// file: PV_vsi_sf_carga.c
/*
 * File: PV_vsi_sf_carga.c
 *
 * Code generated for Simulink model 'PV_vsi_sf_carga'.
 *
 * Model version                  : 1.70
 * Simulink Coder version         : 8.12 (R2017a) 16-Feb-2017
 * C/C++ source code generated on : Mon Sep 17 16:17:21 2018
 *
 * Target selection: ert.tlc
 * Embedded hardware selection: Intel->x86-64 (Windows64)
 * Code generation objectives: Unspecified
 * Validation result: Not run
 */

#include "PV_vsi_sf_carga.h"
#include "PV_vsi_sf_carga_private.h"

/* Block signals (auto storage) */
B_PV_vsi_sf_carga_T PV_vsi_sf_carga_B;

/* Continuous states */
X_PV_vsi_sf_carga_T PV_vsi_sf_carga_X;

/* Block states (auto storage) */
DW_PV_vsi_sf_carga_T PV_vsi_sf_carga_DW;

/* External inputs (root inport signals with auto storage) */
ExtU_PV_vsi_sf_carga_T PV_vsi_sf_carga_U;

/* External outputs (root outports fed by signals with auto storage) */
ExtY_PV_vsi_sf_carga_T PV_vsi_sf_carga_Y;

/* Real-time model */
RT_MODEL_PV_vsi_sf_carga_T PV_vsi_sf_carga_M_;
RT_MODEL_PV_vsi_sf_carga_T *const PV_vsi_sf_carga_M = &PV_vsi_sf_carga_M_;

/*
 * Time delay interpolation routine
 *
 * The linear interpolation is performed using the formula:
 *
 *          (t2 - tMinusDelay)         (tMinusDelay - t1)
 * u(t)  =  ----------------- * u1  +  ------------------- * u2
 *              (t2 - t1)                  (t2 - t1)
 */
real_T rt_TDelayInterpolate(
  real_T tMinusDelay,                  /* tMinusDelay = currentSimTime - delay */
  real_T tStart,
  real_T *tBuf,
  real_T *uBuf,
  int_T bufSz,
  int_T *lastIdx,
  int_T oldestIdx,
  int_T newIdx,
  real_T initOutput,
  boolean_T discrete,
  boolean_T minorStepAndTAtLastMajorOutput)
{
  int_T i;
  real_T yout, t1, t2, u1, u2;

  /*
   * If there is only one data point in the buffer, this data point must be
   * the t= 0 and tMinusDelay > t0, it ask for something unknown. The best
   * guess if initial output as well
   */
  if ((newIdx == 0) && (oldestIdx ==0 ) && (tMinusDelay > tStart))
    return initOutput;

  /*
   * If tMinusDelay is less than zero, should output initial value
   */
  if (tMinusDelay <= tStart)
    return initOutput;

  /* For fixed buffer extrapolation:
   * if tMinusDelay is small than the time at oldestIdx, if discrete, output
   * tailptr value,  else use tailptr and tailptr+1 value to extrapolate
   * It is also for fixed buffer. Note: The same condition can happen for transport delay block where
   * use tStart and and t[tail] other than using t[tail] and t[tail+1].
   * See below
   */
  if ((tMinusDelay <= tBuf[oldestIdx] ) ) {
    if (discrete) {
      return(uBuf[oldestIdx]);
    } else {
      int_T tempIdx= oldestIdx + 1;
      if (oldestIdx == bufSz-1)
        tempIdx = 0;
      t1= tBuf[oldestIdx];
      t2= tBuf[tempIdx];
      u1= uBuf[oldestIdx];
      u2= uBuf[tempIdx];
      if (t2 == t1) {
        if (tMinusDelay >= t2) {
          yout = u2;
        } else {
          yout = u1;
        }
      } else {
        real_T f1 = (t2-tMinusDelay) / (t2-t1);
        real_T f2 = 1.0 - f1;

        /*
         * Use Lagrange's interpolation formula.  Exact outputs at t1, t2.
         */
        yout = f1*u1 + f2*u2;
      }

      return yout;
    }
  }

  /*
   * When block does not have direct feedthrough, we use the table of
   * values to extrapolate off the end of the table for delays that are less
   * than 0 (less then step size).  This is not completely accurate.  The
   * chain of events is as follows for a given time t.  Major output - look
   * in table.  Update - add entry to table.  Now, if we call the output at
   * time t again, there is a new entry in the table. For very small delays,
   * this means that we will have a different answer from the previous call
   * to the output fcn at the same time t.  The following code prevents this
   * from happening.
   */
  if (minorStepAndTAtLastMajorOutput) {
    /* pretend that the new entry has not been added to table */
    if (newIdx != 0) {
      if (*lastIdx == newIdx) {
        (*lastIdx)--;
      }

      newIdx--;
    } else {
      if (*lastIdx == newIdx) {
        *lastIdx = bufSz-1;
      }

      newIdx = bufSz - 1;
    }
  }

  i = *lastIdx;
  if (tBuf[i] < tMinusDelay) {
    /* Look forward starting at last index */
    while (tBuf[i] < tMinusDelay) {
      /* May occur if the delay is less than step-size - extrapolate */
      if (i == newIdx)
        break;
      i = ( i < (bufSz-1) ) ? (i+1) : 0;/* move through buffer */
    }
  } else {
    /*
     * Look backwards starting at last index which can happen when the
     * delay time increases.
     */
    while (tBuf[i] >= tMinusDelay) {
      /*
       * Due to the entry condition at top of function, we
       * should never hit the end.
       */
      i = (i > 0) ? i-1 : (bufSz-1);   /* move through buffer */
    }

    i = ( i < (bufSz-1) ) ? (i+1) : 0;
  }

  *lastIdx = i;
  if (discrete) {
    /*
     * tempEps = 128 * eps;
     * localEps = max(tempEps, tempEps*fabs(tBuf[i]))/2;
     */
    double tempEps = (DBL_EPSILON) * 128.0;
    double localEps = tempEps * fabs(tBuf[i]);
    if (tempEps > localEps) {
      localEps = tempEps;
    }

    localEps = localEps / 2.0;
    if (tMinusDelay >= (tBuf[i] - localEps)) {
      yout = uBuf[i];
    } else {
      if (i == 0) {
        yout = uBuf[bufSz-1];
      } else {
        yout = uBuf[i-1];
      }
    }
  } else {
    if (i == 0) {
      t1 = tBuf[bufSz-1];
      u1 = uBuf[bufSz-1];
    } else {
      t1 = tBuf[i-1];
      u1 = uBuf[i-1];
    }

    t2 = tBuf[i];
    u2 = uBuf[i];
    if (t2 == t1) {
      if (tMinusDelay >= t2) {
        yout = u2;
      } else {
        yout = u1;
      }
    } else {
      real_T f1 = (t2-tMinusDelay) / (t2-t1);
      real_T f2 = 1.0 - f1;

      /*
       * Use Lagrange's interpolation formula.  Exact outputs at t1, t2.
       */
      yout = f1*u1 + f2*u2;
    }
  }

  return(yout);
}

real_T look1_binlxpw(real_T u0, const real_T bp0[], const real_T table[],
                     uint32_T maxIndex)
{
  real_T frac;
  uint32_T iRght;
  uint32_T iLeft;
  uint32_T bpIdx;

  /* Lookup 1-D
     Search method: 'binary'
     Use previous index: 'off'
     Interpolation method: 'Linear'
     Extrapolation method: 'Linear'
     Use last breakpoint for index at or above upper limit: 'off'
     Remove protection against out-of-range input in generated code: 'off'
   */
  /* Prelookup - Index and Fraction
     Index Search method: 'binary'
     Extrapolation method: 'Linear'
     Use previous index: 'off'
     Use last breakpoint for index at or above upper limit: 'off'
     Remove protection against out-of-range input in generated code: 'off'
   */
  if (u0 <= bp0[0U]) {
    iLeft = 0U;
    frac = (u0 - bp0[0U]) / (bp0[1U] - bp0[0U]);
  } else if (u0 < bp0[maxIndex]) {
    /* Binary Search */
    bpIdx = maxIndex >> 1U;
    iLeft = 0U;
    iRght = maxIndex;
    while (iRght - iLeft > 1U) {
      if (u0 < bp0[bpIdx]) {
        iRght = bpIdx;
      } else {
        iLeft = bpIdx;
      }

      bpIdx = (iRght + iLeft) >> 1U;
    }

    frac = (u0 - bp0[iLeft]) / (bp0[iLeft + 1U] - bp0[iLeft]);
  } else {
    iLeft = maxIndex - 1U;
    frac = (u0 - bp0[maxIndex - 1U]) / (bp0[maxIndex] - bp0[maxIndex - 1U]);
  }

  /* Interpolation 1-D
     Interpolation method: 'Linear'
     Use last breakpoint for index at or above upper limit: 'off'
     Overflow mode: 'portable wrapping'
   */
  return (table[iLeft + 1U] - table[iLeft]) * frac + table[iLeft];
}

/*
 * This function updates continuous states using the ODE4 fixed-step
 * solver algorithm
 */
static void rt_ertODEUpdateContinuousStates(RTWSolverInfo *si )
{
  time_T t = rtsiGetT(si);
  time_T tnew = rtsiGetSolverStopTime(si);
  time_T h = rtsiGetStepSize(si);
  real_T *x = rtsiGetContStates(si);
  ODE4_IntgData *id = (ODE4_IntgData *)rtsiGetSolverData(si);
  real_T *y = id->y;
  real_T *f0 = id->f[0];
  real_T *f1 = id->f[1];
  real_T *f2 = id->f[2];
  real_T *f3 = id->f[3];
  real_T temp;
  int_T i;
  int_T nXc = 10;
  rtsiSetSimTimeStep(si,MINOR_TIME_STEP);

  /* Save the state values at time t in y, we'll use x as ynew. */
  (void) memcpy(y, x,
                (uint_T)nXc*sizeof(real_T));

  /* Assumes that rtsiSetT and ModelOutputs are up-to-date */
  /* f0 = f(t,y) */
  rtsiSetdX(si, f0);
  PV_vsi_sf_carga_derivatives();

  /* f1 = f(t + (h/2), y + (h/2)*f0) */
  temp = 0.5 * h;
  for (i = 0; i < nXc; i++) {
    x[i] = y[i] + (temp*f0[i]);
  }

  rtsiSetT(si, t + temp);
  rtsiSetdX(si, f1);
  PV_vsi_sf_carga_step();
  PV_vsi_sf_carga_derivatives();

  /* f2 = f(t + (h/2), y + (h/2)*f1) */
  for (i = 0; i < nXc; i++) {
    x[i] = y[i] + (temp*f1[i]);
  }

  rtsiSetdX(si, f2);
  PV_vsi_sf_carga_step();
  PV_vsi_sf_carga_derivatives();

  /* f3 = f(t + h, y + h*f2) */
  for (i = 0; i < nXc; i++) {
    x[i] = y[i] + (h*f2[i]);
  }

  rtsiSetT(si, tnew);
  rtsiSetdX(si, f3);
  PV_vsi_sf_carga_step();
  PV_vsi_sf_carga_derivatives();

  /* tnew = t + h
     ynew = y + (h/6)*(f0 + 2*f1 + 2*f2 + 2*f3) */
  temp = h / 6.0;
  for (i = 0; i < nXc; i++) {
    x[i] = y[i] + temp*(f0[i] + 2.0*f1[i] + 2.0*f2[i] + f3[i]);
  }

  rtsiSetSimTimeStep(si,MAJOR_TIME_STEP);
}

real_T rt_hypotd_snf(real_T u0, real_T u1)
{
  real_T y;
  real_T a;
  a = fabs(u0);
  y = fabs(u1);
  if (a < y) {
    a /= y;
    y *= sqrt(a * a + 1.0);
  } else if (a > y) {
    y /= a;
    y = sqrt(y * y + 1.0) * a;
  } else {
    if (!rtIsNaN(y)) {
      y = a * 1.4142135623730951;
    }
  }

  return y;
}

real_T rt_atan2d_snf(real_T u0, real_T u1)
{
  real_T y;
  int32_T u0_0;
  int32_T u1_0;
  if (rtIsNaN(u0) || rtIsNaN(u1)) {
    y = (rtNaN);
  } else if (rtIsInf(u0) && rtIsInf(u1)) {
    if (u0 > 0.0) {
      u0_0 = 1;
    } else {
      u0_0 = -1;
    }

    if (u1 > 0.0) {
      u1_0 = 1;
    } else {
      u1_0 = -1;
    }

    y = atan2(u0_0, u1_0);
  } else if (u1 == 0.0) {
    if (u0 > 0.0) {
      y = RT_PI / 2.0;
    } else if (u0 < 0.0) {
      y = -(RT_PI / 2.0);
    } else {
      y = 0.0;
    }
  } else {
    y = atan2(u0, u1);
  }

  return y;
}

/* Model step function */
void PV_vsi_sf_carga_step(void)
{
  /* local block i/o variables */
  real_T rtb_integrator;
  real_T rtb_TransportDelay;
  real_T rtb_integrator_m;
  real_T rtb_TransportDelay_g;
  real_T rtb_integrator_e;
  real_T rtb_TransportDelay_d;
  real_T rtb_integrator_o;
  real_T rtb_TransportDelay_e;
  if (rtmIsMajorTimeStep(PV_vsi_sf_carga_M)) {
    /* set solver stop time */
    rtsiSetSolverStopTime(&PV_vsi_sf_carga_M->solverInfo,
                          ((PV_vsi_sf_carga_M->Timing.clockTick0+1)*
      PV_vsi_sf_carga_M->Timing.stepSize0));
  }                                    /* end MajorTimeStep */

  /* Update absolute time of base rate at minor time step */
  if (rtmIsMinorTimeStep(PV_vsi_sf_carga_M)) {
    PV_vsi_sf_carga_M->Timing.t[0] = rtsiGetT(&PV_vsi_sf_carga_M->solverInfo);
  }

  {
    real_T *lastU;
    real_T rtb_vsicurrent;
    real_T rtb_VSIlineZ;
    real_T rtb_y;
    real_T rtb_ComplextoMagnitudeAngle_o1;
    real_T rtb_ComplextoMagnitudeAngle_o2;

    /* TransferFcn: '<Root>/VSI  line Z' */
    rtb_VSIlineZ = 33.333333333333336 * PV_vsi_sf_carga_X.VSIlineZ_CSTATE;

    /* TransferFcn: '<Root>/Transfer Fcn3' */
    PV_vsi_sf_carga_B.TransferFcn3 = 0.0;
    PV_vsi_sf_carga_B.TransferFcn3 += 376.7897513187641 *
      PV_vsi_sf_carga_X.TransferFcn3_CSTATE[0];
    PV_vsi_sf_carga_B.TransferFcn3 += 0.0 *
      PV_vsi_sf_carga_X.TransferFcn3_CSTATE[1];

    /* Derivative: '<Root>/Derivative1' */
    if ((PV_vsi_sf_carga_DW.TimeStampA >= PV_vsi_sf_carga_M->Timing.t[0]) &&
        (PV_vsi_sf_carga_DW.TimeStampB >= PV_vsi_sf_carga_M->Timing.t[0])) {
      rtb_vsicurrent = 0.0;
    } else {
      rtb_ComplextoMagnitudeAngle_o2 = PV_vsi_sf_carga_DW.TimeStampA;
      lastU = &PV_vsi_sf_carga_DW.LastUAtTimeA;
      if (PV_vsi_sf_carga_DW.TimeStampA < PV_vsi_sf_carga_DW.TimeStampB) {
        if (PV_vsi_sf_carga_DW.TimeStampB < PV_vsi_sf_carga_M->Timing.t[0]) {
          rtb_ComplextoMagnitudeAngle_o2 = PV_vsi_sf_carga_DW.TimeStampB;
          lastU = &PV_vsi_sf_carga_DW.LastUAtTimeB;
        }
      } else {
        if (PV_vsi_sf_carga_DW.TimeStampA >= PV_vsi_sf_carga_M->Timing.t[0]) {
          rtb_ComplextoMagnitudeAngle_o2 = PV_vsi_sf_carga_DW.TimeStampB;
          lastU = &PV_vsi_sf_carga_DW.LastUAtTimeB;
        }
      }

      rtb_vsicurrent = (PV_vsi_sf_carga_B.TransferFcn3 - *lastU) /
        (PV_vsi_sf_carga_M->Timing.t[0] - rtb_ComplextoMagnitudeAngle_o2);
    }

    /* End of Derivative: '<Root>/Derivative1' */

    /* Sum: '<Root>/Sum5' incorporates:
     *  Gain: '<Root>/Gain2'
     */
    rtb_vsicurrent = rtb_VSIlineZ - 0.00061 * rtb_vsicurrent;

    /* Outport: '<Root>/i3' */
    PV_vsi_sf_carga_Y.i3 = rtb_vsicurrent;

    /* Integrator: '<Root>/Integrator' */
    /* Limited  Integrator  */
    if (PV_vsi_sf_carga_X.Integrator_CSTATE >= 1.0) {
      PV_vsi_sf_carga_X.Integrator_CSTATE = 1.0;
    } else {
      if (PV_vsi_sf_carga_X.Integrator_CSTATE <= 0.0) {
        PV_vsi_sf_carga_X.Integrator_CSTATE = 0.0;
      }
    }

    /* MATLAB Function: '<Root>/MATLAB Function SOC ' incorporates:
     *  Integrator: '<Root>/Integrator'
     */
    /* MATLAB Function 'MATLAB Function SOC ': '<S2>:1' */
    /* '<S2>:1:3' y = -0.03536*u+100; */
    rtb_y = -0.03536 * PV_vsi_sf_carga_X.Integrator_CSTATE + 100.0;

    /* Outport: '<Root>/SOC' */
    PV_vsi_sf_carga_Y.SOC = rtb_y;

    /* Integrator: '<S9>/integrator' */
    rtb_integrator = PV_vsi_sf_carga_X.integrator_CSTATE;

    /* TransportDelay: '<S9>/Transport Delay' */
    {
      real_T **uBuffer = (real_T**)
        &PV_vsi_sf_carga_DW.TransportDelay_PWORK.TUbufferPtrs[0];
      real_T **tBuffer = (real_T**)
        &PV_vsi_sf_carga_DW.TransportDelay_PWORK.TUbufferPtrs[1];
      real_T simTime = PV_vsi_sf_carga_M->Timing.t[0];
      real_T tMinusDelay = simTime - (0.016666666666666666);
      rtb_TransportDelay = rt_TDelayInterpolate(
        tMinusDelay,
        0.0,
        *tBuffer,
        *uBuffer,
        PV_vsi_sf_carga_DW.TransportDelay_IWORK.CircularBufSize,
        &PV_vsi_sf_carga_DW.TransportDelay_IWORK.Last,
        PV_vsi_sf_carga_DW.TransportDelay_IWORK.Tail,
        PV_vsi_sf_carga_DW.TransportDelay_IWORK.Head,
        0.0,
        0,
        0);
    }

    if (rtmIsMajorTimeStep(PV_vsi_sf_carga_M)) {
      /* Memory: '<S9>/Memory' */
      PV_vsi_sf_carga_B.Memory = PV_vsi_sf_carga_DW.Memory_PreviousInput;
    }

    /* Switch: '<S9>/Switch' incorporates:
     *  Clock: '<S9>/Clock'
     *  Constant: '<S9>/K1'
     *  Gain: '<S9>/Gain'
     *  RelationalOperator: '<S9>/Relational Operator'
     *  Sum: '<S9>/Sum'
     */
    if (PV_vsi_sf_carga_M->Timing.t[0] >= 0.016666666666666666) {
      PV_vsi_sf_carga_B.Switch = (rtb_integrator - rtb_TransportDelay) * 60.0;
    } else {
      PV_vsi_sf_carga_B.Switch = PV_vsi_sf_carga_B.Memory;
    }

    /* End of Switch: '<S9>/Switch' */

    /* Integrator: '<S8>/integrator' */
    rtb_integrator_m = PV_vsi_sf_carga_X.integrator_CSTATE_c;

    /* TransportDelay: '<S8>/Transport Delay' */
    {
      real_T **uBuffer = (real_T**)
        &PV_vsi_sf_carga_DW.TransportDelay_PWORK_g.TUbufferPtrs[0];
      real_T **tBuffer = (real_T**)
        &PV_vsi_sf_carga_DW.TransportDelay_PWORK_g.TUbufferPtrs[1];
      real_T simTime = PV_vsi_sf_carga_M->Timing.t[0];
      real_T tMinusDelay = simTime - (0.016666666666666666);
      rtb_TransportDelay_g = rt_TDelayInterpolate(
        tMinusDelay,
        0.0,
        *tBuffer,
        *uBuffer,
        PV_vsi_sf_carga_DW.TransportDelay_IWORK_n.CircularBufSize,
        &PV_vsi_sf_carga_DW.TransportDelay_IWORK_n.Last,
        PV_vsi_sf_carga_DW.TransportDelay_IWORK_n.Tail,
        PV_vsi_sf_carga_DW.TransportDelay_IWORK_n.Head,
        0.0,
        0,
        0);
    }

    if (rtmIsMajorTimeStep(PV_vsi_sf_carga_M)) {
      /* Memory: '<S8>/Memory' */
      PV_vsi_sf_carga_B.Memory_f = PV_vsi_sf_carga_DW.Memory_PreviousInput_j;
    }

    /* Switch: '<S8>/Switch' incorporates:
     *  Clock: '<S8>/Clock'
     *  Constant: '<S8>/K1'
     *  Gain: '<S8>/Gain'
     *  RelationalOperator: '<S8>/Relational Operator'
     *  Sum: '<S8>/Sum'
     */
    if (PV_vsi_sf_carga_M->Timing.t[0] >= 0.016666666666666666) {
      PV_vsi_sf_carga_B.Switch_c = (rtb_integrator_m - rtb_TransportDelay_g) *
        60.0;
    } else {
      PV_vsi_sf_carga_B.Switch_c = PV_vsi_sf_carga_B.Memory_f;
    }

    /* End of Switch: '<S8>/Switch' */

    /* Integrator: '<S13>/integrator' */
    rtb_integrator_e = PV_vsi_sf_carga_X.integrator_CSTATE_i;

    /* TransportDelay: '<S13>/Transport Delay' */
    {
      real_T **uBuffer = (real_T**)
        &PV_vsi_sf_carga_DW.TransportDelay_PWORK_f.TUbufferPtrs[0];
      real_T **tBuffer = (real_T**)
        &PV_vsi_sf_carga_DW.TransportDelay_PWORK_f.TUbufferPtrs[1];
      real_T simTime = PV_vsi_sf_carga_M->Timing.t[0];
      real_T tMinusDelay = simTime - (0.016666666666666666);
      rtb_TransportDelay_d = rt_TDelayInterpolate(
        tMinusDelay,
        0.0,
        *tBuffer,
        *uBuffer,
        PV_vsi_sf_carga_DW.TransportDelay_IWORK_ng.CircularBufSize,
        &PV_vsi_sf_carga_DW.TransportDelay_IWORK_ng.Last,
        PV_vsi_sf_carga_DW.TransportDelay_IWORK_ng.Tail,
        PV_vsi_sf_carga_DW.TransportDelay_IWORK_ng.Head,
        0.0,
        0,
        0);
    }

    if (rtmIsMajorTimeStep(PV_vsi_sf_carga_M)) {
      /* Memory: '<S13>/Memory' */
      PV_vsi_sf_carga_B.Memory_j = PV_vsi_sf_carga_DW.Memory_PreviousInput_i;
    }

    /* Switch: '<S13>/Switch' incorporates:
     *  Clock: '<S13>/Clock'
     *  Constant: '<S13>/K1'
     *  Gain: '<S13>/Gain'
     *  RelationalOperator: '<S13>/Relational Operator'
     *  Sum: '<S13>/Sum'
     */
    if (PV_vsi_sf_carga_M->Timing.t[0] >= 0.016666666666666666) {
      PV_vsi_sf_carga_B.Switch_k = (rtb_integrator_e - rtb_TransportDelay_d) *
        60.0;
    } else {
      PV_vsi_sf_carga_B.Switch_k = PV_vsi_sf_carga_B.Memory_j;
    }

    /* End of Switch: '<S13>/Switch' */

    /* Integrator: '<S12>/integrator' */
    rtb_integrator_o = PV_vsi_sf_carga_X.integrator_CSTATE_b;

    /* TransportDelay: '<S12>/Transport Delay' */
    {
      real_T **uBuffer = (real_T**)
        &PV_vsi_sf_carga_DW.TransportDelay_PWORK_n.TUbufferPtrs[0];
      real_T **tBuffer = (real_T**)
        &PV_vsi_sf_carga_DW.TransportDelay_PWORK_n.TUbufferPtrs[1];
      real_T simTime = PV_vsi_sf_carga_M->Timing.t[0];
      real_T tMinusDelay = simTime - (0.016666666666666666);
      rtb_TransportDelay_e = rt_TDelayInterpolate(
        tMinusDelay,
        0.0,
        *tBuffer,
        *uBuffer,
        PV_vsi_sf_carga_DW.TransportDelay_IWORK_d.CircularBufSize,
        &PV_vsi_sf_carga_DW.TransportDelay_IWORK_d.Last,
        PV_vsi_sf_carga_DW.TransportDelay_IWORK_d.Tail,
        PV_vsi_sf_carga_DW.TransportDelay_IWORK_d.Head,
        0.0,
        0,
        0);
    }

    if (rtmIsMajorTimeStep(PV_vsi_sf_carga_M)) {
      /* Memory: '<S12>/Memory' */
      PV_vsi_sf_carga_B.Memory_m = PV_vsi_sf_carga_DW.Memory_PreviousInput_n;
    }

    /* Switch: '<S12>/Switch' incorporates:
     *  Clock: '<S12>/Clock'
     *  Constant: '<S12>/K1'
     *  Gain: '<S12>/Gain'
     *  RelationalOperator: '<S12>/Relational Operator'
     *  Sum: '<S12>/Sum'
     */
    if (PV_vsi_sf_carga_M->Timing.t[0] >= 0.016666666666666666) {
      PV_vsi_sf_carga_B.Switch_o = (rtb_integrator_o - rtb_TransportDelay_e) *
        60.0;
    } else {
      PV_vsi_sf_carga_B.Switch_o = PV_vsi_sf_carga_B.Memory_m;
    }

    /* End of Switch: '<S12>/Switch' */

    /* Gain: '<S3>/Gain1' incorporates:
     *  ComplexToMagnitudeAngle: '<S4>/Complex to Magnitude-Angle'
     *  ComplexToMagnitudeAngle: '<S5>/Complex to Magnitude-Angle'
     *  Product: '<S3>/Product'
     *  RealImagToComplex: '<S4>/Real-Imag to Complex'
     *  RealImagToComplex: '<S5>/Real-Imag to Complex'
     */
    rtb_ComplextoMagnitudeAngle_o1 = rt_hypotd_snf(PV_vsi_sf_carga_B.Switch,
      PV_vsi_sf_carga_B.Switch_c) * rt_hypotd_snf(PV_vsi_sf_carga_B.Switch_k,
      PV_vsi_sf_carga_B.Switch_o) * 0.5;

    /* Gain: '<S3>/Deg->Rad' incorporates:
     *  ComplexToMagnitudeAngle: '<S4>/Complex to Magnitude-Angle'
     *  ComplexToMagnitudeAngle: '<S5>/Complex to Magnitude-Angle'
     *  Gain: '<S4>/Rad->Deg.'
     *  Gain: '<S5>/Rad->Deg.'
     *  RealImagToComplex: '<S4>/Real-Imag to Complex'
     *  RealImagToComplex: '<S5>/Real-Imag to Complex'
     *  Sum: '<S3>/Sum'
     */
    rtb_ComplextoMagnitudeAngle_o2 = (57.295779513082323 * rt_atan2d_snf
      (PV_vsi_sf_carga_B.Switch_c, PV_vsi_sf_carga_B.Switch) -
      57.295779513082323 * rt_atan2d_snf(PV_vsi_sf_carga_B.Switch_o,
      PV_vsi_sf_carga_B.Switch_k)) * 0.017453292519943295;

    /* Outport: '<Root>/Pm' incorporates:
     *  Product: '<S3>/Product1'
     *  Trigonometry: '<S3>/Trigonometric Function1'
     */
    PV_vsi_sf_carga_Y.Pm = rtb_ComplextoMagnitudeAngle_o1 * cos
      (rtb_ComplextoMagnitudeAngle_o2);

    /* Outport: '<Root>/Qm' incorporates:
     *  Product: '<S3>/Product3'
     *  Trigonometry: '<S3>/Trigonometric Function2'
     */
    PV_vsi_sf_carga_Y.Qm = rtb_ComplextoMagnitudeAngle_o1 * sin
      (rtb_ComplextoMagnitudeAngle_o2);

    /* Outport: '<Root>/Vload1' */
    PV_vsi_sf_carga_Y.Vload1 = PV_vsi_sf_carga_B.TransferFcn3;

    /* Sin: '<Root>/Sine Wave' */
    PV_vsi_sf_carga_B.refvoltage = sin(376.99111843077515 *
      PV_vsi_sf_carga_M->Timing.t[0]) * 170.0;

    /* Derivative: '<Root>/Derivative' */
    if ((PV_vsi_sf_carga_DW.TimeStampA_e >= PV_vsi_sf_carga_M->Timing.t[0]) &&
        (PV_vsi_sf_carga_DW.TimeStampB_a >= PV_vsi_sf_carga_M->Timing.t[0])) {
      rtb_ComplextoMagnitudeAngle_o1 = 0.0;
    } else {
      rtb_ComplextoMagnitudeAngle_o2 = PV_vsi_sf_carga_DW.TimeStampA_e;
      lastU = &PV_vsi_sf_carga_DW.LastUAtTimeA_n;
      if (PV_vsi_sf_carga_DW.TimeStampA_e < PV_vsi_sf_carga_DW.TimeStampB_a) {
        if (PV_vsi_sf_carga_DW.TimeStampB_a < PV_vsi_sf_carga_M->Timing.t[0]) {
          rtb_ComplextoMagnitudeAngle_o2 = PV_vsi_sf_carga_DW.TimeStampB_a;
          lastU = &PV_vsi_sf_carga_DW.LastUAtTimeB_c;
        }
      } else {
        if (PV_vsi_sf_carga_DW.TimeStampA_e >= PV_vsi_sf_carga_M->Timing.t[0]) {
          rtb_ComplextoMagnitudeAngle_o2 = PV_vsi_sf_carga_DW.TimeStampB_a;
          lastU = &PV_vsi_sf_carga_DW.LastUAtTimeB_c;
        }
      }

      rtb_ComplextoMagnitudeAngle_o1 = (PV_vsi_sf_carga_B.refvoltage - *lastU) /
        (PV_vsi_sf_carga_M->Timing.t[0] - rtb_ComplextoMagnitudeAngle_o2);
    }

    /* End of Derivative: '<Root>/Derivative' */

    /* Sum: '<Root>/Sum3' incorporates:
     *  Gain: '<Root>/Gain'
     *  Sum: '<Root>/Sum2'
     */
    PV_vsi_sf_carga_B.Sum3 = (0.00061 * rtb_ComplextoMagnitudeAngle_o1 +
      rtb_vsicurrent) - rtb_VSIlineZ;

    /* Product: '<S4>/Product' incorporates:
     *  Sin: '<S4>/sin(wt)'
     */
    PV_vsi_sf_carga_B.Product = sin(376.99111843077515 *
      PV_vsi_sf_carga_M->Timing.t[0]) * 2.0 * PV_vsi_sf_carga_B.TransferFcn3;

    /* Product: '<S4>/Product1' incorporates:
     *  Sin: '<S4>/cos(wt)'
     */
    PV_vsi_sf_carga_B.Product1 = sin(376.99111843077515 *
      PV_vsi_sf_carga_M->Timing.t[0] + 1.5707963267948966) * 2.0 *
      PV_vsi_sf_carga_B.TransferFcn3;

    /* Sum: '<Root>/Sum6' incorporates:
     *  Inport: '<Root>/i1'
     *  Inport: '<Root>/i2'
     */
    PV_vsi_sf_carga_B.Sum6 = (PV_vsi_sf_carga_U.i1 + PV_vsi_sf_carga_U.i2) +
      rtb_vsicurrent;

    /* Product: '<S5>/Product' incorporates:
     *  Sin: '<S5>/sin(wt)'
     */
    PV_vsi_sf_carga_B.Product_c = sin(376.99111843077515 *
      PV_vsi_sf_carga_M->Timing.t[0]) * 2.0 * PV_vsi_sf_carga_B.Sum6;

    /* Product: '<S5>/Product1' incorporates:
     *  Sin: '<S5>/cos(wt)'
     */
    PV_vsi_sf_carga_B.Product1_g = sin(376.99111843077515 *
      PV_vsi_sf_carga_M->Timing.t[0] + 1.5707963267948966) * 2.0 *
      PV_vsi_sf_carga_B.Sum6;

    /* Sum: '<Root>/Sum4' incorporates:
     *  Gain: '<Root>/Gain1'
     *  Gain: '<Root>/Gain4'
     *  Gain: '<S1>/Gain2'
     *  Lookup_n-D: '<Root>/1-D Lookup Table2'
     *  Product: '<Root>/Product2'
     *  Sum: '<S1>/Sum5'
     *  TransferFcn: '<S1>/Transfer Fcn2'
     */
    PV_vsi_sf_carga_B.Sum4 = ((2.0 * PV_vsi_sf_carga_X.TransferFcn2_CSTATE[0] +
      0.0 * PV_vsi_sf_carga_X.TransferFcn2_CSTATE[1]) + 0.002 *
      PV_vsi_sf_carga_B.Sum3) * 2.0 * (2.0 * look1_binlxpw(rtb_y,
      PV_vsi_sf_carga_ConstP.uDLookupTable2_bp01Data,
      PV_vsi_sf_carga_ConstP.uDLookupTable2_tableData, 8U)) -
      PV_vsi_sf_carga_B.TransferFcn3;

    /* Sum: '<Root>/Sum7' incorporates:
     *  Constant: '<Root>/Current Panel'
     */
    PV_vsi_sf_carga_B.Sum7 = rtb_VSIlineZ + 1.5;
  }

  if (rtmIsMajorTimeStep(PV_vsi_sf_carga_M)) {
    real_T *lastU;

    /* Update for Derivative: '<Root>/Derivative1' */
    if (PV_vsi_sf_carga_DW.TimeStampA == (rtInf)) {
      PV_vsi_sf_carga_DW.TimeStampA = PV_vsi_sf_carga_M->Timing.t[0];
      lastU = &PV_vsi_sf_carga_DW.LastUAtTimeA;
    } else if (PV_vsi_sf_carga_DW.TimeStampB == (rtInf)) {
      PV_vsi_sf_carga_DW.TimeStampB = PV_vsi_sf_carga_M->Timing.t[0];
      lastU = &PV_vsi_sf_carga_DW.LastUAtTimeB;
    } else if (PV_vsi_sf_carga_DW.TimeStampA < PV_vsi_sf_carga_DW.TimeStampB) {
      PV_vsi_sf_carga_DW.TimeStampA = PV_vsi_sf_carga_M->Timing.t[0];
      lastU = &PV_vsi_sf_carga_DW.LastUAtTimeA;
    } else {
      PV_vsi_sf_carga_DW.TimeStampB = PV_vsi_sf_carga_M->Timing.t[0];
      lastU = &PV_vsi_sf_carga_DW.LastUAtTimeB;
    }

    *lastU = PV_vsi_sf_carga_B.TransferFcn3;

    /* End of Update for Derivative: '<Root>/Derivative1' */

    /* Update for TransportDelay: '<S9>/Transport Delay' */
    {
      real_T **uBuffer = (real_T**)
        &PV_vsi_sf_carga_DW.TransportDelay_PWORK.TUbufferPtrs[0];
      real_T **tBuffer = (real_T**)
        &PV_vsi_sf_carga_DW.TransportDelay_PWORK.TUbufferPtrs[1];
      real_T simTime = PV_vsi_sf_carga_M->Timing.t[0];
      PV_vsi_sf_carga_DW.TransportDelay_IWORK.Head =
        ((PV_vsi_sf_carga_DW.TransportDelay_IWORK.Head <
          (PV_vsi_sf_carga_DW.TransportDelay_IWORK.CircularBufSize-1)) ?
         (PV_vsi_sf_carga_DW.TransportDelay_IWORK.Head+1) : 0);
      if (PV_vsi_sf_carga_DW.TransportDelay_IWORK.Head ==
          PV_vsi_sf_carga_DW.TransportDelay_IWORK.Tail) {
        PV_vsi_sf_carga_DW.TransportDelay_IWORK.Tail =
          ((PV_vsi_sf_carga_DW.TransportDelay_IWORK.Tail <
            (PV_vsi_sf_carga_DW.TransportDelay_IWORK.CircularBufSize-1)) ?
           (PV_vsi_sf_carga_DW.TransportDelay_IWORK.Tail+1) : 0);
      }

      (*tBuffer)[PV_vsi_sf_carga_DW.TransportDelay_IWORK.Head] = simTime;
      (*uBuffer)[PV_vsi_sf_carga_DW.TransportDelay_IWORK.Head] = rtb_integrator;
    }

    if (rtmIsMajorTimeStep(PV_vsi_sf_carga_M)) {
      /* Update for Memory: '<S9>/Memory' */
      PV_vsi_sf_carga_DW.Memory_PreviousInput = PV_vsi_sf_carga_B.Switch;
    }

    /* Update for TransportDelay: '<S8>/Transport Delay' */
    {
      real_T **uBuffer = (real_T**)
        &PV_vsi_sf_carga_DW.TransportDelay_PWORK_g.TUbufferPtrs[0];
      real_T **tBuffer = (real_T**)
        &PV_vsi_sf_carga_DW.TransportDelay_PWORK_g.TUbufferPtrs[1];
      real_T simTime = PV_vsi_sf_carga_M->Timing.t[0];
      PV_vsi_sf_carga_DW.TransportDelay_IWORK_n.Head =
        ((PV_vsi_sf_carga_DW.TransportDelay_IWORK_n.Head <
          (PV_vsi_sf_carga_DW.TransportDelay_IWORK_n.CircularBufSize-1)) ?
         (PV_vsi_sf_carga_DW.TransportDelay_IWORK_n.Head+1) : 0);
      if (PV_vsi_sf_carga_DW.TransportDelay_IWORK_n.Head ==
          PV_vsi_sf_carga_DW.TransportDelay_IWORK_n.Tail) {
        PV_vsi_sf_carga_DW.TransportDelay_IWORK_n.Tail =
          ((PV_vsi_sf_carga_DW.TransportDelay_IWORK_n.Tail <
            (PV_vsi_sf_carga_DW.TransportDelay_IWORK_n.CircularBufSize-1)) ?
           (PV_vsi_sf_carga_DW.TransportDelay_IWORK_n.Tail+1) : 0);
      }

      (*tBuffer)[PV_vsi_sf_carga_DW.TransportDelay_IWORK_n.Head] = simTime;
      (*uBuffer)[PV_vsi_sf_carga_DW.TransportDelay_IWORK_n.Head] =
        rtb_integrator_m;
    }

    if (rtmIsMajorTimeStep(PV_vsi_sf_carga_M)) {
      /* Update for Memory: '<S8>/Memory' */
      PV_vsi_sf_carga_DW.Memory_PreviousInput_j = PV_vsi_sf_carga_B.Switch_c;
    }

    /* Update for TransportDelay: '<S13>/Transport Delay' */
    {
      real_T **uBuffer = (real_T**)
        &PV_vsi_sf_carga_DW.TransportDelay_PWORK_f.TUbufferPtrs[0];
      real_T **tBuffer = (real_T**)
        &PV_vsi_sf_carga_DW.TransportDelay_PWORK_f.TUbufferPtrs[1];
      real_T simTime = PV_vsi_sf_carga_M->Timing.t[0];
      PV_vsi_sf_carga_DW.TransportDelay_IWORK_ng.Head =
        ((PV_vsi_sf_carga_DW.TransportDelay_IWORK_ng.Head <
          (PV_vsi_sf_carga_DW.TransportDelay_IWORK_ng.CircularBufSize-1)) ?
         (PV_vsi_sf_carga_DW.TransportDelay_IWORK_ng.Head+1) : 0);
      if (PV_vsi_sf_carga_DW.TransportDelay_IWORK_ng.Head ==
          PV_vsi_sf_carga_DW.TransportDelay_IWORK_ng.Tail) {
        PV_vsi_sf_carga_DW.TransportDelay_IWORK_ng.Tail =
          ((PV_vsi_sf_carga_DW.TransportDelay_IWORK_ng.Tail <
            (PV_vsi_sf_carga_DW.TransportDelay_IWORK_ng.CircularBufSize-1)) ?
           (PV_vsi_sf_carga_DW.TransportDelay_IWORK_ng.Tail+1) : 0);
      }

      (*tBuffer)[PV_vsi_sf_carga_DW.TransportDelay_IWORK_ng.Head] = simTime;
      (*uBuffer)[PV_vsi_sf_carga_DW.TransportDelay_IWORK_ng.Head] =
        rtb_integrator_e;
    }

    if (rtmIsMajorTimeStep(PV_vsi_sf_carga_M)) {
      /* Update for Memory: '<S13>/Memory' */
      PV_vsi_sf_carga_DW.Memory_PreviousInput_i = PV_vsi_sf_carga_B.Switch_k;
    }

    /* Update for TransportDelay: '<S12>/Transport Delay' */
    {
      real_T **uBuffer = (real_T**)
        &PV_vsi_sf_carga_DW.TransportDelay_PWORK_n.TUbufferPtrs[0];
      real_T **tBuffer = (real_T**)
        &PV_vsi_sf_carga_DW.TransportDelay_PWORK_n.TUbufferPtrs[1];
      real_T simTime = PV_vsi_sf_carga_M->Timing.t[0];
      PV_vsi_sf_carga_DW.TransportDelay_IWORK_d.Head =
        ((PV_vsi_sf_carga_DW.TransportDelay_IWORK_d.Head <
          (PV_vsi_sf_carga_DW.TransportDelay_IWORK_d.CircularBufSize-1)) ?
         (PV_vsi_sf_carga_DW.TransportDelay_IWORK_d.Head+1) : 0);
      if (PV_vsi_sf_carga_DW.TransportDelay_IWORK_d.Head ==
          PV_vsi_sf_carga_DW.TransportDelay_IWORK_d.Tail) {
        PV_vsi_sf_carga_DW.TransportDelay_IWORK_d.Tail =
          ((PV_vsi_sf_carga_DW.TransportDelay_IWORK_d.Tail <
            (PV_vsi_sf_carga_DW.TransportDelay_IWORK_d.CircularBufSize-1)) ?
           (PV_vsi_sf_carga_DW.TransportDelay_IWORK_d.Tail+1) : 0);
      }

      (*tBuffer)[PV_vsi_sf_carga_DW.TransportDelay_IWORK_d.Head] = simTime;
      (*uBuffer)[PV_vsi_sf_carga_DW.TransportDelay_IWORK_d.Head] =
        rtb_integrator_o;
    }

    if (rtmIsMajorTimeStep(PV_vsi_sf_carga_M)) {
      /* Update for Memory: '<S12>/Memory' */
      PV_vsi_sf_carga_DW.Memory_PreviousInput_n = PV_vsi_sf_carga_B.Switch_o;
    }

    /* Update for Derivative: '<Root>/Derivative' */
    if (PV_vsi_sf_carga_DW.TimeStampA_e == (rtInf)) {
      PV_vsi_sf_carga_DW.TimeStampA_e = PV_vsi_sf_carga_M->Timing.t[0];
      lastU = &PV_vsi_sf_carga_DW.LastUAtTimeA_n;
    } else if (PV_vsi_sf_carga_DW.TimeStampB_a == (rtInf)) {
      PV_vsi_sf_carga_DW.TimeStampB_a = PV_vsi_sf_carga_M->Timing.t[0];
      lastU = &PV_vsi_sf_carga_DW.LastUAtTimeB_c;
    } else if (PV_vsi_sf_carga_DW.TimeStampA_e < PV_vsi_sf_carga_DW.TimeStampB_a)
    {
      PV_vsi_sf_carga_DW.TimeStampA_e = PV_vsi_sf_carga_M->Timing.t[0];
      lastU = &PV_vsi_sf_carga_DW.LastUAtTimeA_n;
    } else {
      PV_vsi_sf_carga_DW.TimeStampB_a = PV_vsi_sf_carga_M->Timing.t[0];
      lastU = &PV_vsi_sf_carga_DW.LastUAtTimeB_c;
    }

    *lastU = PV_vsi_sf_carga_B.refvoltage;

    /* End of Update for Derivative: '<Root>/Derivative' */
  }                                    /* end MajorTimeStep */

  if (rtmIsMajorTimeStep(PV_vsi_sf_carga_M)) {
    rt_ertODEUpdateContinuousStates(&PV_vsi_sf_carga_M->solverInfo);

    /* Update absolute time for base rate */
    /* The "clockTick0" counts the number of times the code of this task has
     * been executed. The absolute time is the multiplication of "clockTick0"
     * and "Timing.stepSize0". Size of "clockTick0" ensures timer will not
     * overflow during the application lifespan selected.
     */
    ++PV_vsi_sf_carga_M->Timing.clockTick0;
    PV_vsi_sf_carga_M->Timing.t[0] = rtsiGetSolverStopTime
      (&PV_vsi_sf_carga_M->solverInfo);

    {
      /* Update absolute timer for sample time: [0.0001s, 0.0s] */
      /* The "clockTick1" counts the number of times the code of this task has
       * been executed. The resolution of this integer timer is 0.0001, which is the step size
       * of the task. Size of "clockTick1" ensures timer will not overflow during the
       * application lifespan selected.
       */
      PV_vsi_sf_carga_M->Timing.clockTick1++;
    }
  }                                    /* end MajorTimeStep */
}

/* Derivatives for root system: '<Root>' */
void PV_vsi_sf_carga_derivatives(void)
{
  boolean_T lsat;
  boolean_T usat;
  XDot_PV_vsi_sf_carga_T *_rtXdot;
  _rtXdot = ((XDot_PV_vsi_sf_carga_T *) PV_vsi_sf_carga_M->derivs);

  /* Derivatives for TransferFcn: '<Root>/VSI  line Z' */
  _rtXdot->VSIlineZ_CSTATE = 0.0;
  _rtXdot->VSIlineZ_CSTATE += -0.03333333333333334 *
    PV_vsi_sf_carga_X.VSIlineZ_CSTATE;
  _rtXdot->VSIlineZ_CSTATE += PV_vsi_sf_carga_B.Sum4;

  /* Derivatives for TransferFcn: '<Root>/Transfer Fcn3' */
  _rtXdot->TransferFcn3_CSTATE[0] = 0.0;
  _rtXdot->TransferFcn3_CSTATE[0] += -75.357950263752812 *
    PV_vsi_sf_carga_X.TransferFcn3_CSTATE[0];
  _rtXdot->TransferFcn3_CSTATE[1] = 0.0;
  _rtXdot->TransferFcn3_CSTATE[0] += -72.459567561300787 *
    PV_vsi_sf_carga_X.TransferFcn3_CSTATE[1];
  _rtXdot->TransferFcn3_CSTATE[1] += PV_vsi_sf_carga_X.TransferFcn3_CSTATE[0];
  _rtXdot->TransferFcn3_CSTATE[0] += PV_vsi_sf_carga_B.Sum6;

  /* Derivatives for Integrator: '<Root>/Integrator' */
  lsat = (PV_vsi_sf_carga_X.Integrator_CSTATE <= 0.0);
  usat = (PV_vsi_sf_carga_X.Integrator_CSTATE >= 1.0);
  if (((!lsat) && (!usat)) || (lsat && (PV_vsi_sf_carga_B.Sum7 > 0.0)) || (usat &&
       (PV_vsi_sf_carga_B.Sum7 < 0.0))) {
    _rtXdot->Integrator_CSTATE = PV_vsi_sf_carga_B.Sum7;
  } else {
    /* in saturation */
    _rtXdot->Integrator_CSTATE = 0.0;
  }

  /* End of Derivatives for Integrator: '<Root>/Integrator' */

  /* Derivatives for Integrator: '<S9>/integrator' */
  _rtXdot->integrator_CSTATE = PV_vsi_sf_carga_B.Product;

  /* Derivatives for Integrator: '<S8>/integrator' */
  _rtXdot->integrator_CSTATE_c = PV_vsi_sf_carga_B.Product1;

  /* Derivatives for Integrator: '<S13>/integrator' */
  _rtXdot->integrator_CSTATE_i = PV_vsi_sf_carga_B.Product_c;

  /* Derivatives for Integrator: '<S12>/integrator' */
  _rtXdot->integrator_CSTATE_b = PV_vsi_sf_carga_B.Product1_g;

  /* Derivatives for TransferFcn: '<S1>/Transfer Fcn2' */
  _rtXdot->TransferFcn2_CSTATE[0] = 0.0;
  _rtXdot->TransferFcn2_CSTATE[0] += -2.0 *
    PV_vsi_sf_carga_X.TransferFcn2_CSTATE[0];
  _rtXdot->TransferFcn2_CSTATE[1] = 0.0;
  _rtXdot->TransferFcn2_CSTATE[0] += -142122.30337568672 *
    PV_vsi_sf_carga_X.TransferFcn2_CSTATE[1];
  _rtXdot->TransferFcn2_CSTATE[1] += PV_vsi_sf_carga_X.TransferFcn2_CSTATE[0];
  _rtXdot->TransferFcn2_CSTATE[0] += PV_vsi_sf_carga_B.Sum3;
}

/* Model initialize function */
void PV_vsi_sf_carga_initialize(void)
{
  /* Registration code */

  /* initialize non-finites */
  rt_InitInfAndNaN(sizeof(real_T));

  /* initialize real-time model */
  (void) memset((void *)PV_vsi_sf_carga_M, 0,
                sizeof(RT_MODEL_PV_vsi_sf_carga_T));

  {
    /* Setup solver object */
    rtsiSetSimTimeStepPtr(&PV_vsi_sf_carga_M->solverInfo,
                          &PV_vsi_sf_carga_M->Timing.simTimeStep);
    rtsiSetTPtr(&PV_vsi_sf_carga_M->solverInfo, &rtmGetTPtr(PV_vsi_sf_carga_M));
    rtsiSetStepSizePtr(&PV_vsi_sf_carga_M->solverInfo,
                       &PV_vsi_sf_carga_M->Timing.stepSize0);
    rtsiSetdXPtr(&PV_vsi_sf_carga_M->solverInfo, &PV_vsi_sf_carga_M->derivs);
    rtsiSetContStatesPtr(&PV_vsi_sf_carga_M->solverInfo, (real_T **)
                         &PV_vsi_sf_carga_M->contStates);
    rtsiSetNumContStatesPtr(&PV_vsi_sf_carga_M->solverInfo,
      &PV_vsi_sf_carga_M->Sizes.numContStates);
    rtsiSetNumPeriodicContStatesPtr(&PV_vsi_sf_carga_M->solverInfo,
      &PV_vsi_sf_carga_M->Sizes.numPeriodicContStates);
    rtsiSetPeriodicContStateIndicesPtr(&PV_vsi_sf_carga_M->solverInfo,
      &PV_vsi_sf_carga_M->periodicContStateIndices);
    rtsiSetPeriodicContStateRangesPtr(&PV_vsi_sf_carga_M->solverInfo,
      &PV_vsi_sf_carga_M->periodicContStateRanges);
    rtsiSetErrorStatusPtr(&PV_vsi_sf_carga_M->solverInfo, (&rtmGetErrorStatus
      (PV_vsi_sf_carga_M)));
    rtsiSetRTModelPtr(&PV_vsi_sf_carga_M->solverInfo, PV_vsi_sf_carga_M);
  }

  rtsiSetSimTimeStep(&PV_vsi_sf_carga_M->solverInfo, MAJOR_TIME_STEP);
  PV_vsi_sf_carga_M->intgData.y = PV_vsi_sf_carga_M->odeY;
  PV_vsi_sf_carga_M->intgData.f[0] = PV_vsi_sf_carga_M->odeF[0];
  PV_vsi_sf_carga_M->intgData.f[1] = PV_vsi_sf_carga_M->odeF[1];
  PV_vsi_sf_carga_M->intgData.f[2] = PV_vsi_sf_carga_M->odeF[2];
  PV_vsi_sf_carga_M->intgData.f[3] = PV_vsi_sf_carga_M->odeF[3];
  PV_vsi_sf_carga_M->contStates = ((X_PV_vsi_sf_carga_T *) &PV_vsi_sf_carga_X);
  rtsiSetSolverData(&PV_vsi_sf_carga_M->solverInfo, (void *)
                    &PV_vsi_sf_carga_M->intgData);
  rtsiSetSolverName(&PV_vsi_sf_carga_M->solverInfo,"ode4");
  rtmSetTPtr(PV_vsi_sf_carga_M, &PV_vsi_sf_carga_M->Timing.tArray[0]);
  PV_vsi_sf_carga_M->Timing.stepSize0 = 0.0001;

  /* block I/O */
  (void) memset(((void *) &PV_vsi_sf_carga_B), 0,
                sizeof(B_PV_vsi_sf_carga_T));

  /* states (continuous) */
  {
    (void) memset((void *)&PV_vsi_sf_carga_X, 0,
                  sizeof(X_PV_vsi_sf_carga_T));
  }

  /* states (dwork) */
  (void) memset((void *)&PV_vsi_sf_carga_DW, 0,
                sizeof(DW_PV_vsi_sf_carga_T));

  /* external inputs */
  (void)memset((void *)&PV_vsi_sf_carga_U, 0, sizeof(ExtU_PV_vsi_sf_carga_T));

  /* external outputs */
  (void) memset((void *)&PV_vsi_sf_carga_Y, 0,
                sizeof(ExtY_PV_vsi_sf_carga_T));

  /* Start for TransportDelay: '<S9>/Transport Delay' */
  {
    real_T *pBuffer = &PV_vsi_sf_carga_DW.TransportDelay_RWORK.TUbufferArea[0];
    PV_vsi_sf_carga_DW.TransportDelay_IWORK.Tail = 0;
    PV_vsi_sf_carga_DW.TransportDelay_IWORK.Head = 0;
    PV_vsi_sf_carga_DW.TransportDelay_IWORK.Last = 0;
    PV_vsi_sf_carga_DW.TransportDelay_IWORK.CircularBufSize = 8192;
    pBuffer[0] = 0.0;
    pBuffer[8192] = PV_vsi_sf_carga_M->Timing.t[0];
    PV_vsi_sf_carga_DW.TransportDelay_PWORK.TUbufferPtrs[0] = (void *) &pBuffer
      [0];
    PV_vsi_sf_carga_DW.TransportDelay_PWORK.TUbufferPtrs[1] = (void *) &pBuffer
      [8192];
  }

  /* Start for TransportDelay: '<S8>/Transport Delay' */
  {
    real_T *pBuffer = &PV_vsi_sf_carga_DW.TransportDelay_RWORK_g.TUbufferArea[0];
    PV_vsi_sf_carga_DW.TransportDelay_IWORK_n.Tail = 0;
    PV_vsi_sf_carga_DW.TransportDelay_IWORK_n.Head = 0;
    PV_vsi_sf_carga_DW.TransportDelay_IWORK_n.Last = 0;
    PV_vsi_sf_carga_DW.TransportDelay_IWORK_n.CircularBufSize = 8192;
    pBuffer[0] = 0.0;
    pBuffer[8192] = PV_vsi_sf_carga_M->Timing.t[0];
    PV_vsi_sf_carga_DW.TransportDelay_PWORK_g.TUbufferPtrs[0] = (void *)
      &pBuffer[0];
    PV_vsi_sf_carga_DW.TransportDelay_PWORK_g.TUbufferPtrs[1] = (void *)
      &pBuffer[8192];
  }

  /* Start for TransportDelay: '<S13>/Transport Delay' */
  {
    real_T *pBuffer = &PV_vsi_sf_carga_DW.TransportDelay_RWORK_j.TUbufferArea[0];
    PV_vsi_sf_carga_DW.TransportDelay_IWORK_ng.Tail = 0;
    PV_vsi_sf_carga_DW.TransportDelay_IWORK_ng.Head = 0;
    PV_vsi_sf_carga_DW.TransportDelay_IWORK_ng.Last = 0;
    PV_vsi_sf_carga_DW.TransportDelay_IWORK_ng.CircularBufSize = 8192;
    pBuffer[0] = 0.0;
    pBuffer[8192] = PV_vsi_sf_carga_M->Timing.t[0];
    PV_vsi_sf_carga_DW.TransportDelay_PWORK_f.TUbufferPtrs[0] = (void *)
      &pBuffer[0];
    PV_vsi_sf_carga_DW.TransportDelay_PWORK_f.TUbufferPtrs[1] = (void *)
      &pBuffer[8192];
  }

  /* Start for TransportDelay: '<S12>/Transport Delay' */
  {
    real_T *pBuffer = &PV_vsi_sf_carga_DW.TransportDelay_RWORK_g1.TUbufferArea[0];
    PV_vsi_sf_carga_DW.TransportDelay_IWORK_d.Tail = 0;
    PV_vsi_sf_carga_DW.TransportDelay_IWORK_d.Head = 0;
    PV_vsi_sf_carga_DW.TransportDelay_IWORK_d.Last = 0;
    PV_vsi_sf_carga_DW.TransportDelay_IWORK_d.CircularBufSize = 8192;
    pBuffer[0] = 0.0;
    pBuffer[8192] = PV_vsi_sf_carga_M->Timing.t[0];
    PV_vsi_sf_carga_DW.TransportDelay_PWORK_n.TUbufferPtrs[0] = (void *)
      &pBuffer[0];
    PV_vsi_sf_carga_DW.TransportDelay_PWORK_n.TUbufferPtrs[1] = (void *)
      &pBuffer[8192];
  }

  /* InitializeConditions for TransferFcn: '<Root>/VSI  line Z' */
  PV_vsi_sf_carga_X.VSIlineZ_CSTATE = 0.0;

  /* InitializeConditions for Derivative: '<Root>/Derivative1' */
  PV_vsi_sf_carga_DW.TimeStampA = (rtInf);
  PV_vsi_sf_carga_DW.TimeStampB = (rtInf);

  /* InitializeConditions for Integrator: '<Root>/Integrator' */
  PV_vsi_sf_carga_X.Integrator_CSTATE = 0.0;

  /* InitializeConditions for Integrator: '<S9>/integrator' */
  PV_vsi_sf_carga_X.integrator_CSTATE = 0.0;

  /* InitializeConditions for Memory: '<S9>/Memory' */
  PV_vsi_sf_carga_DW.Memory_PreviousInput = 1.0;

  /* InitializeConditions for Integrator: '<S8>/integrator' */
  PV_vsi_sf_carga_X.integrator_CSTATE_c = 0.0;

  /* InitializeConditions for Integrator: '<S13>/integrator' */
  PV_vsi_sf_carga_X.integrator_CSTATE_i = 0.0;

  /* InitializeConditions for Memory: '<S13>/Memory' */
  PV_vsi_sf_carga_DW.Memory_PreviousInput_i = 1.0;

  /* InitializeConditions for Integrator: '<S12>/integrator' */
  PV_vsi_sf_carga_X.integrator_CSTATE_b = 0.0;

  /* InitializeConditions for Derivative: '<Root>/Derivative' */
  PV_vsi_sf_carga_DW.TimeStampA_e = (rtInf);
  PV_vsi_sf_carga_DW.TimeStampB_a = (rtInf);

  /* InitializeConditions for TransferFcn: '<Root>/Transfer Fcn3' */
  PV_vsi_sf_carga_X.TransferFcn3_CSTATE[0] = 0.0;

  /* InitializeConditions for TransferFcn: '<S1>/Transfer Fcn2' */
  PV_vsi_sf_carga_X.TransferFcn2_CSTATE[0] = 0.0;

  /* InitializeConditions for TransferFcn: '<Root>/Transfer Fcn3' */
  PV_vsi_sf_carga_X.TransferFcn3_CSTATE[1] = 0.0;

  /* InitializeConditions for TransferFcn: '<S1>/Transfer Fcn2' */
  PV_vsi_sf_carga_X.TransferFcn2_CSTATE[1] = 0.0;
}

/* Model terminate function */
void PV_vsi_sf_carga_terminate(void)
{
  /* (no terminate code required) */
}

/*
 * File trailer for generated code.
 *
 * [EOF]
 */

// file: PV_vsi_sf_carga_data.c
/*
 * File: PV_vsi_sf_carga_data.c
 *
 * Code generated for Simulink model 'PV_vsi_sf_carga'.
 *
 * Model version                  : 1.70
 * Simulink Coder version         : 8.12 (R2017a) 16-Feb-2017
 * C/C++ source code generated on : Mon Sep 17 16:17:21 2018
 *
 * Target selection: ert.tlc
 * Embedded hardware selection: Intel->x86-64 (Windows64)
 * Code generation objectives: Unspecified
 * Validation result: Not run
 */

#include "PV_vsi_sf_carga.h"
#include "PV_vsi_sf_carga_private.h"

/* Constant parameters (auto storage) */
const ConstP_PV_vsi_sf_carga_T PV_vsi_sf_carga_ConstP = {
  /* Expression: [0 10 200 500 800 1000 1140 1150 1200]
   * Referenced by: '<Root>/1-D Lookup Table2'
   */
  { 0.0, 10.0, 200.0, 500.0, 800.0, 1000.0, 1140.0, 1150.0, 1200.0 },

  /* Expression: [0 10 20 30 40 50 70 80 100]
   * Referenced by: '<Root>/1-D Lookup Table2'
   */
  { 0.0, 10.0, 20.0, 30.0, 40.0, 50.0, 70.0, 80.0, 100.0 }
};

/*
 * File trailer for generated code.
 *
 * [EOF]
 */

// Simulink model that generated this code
simulink model "PV_vsi_sf_carga"  (R2017a)
settings: Solver=ode4  StartTime=0.0  StopTime=6  FixedStep=1e-4  RelTol=1e-3
InitFcn:
  | SimulinkInit
values from neighbouring files (symbols this model uses):
  C = [C11; C22; C33;C44]    [Parametros_Sistema.m]    (also in SimulinkInit.m = 0.002654; SimulinkInit_linea_transmision.m = 1)
  C3 = 610e-6    (= 0.00061)    [Parametros_Sistema.m]    (also in SimulinkInit.m; SimulinkInit_linea_transmision.m; sistema.m)
  L3 = 5e-3    (= 0.005)    [Parametros_Sistema.m]    (also in SimulinkInit.m = 0.03; SimulinkInit_linea_transmision.m; sistema.m)
  L4 = 1e-3    (= 0.001)    [Parametros_Sistema.m]    (also in SimulinkInit.m = 5.2; SimulinkInit_linea_transmision.m = 3.5e-05; sistema.m)
  R3 = 1e-3    (= 0.001)    [Parametros_Sistema.m]    (also in SimulinkInit.m; SimulinkInit_linea_transmision.m; sistema.m)
  R4 = 10    [Parametros_Sistema.m]    (also in SimulinkInit.m; SimulinkInit_linea_transmision.m = 0.005; sistema.m)
  R5 = 4    [Parametros_Sistema.m]    (also in SimulinkInit.m = 10; SimulinkInit_linea_transmision.m = 0.0012; sistema.m)
libraries: powerlib_meascontrol x1

== system PV_vsi_sf_carga ==
  note: VSI
  note: Carga RLC
  Vload : Inport
  Ipv : Inport  Port=2
  i1 : Inport  Port=3
  i2 : Inport  Port=4
  1-D Lookup Table2 : Lookup_n-D  NumberOfTableDimensions=1  BreakpointsForDimension1=[0 10 20 30 40 50 70 80 100]  Table=[0 10 200 500 800 1000 1140 1150 1200]  InternalRulePriority=Speed  RndMeth=Simplest  InputSameDT=on
  Control PR VSI : Subsystem
  Current Panel : Constant  Value=1.5
  Derivative : Derivative
  Derivative1 : Derivative
  Gain : Gain  Gain=C3
  Gain1 : Gain  Gain=2
  Gain2 : Gain  Gain=C3
  Gain4 : Gain  Gain=2
  Integrator : Integrator  LimitOutput=on  UpperSaturationLimit=1  LowerSaturationLimit=0
  "MATLAB Function SOC " : MATLAB Function  TreatAsAtomicUnit=on
  Power : powerlib_meascontrol/Measurements/Power  Freq=60  Vinit=[1, 0]  Iinit=[1, 0]  Ts=0
  Product2 : Product
  Sine Wave : Sin  Amplitude=170  Frequency=2*pi*60  SampleTime=0
  Sum2 : Sum  Inputs=|++
  Sum3 : Sum  Inputs=|+-
  Sum4 : Sum  Inputs=|+-
  Sum5 : Sum  Inputs=|+-
  Sum6 : Sum  Inputs=3
  Sum7 : Sum  Inputs=|++
  Transfer Fcn3 : TransferFcn  Numerator=[R4*R5*L4 0]  Denominator=[C*R4*R5*L4 (R4+R5)*L4 R4*R5]
  VSI  line Z : TransferFcn  Denominator=[L3 R3]
  i3 : Outport
  SOC : Outport  Port=2
  Pm : Outport  Port=3
  Qm : Outport  Port=4
  Vload1 : Outport  Port=5
  wires:
  Sine Wave/1 -> Derivative/1  "ref voltage"
  Derivative/1 -> Gain/1
  Gain/1 -> Sum2/1  "cap Iref"
  Sum2/1 -> Sum3/1  "inductor Iref"
  Sum3/1 -> Control PR VSI/1(Ierror)
  Control PR VSI/1(d) -> Gain1/1
  Gain1/1 -> Product2/1
  Product2/1 -> Sum4/1
  Derivative1/1 -> Gain2/1
  Sum4/1 -> VSI  line Z/1
  VSI  line Z/1 -> [ipi], Sum5/1
  Gain2/1 -> Sum5/2  "cap current"
  Sum5/1 -> i3/1, [i3]  "vsi current"
  [ipi] -> Sum7/1, Sum3/2  "inductor I measured"
  [i3] -> Sum2/2
  Integrator/1 -> "MATLAB Function SOC "/1(u)
  "MATLAB Function SOC "/1(y) -> SOC/1, 1-D Lookup Table2/1  "soc"
  1-D Lookup Table2/1 -> Gain4/1  "battery Vdc"
  Gain4/1 -> Product2/2
  Sum7/1 -> Integrator/1
  [Vload] -> Derivative1/1, Sum4/2
  Current Panel/1 -> Sum7/2
  Transfer Fcn3/1 -> [Vload], Vload1/1, Power/1
  i2/1 -> Sum6/2
  Sum6/1 -> [I_load], Transfer Fcn3/1
  Power/1 -> Pm/1
  i1/1 -> Sum6/1
  [I_load] -> Power/2
  Power/2 -> Qm/1
  [i3] -> Sum6/3

== system PV_vsi_sf_carga/Control PR VSI ==
  Ierror : Inport
  Constant2 : Constant  Value=0
  Gain2 : Gain  Gain=.002
  Sum5 : Sum  Inputs=+|+
  Sum9 : Sum  Inputs=|++
  Transfer Fcn2 : TransferFcn  Numerator=[2 0]  Denominator=[1 2 (2*pi*60)^2]
  d : Outport
  wires:
  Constant2/1 -> Sum9/2
  Sum5/1 -> Sum9/1
  Transfer Fcn2/1 -> Sum5/2
  Gain2/1 -> Sum5/1
  Ierror/1 -> Transfer Fcn2/1, Gain2/1
  Sum9/1 -> d/1

== matlab function PV_vsi_sf_carga/MATLAB Function SOC  ==
function y = fcn(u)

y = -0.03536*u+100;
